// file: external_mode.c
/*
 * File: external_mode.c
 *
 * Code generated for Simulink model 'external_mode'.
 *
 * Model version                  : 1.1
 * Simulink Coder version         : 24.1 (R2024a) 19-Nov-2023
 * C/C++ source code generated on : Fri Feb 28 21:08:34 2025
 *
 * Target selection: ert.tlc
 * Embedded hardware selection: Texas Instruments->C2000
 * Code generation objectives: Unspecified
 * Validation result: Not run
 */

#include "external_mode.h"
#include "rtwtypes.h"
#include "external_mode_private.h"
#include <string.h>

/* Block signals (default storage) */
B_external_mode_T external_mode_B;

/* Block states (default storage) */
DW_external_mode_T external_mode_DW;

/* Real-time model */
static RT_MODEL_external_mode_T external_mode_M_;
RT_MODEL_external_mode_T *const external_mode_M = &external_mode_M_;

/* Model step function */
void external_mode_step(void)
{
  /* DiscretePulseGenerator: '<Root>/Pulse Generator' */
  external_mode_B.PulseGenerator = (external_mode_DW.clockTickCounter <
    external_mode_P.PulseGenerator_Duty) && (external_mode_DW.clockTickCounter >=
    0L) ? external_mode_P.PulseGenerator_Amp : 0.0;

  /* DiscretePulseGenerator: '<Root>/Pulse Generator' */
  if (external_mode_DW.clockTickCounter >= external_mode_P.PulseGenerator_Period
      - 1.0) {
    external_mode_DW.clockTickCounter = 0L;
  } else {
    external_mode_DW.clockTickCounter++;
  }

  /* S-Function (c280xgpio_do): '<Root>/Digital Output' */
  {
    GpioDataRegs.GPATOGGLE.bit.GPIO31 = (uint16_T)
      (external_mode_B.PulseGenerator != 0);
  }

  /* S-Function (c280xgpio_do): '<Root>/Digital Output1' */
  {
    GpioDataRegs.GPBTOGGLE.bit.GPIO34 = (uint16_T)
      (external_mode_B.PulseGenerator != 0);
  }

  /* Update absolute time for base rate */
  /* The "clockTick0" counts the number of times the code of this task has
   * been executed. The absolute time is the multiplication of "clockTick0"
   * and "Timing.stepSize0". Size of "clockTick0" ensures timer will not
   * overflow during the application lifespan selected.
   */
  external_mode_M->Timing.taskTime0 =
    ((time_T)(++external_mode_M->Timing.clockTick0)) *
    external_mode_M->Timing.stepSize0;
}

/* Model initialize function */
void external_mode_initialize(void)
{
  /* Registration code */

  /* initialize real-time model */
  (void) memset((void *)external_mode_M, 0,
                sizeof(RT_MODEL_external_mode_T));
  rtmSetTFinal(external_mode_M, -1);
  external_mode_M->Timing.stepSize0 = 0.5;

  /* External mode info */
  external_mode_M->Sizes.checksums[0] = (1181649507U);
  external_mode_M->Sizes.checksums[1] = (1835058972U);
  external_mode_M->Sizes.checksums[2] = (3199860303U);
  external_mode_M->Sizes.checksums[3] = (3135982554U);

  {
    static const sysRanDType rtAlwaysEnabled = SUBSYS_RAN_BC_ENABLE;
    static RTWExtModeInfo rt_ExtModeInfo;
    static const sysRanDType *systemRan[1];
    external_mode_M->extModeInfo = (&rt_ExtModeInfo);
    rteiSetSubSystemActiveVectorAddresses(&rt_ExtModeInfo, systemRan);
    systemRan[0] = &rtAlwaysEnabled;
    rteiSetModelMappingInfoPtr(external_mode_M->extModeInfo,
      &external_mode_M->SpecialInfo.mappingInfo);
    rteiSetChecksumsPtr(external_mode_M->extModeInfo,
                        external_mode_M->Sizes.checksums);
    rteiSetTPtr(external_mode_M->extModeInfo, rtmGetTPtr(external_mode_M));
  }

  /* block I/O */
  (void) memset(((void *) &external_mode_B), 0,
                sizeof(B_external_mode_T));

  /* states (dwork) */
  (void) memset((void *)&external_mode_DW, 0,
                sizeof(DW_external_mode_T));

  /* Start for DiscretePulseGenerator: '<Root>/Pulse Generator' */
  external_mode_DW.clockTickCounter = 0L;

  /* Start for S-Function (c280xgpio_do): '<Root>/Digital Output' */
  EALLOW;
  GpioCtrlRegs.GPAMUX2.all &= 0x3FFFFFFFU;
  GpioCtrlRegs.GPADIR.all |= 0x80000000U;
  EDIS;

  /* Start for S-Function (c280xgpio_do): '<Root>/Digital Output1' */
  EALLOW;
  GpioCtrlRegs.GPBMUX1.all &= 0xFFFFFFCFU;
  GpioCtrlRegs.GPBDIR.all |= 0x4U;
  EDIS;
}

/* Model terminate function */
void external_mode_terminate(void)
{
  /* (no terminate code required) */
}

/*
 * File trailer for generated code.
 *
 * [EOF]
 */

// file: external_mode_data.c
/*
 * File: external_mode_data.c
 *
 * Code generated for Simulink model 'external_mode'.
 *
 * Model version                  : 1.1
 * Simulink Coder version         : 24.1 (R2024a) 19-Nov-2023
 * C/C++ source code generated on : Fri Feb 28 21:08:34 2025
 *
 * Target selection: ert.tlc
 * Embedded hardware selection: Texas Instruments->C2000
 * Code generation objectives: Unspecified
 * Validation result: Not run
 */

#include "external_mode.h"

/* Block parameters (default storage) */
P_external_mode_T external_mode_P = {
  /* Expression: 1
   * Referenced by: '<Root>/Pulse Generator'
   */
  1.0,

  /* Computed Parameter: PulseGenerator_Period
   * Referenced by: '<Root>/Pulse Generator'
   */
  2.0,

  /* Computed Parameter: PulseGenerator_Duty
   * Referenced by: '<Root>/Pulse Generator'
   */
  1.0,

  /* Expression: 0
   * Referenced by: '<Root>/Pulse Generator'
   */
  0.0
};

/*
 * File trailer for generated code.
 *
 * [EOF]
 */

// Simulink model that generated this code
simulink model "external_mode"  (R2024a)
settings: Solver=FixedStepAuto  StartTime=0.0  StopTime=Inf  RelTol=1e-3  EnableMultiTasking=on
libraries: c2837xDlib x2

== system external_mode ==
  Digital Output : c2837xDlib/Digital Output  GPIO_Number=GPIO24~GPIO31  GPIO_Bit0=off  GPIO_BIT0_Toggle=off  GPIO_Bit1=off  GPIO_BIT1_Toggle=off  GPIO_Bit2=off  GPIO_BIT2_Toggle=off  GPIO_Bit3=off  GPIO_BIT3_Toggle=off  GPIO_Bit4=off  GPIO_BIT4_Toggle=off  GPIO_Bit5=off  GPIO_BIT5_Toggle=off  GPIO_Bit6=off  GPIO_BIT6_Toggle=off  GPIO_Bit7=on  GPIO_BIT7_Toggle=on
  Digital Output1 : c2837xDlib/Digital Output  GPIO_Number=GPIO32~GPIO39  GPIO_Bit0=off  GPIO_BIT0_Toggle=on  GPIO_Bit1=off  GPIO_BIT1_Toggle=off  GPIO_Bit2=on  GPIO_BIT2_Toggle=on  GPIO_Bit3=off  GPIO_BIT3_Toggle=off  GPIO_Bit4=off  GPIO_BIT4_Toggle=off  GPIO_Bit5=off  GPIO_BIT5_Toggle=off  GPIO_Bit6=off  GPIO_BIT6_Toggle=off  GPIO_Bit7=off  GPIO_BIT7_Toggle=off
  Pulse Generator : DiscretePulseGenerator  PulseType=Time based  Period=0.5  PulseWidth=80
  Scope : Scope
  wires:
  Pulse Generator/1 -> Scope/1, Digital Output1/1, Digital Output/1
